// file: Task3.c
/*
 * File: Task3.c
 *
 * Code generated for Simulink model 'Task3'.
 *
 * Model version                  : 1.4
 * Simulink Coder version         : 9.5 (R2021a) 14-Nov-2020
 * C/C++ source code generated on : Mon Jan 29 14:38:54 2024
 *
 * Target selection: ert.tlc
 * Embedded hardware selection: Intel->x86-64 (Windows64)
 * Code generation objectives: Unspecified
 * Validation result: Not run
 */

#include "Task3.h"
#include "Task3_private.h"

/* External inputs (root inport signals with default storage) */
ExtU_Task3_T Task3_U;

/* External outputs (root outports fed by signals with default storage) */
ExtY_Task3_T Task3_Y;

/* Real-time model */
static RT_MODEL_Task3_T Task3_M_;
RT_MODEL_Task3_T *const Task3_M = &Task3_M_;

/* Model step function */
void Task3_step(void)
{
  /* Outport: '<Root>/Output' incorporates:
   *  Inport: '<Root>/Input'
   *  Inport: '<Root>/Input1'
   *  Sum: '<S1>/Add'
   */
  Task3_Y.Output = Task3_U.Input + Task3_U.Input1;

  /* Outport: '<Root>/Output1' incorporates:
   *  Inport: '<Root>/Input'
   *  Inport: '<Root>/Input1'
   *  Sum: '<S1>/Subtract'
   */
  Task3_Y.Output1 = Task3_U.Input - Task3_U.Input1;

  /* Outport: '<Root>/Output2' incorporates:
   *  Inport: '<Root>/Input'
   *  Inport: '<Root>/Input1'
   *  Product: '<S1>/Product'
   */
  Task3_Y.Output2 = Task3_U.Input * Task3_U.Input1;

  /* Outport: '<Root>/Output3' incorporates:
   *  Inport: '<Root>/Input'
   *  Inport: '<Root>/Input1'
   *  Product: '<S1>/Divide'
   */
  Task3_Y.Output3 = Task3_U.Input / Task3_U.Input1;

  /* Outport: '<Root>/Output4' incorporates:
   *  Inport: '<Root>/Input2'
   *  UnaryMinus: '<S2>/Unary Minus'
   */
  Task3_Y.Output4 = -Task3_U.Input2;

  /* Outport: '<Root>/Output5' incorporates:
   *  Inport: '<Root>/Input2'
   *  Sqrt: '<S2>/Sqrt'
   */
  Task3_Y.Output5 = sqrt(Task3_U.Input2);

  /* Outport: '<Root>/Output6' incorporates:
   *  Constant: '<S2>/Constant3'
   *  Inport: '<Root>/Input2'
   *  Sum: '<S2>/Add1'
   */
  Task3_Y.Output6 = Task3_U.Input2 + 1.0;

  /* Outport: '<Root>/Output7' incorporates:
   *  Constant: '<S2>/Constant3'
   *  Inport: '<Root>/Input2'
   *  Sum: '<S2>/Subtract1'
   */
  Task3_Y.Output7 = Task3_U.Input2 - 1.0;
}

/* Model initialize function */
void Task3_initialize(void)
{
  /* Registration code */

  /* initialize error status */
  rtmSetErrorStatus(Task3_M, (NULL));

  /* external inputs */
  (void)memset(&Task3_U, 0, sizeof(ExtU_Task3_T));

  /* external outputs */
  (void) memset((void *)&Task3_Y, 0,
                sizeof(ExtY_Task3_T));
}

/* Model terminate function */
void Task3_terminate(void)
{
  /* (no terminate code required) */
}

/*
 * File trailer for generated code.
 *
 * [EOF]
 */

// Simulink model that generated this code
simulink model "Task3"  (R2021a)
settings: Solver=FixedStepDiscrete  StartTime=0.0  StopTime=10.0  RelTol=1e-3  EnableMultiTasking=on

== system Task3 ==
  Input : Inport
  Input1 : Inport  Port=2
  Input2 : Inport  Port=3
  Subsystem : Subsystem
  Subsystem1 : Subsystem
  Output : Outport
  Output1 : Outport  Port=2
  Output2 : Outport  Port=3
  Output3 : Outport  Port=4
  Output4 : Outport  Port=5
  Output5 : Outport  Port=6
  Output6 : Outport  Port=7
  Output7 : Outport  Port=8
  wires:
  Input/1 -> Subsystem/1(In1)
  Input1/1 -> Subsystem/2(In2)
  Subsystem/1(Out1) -> Output/1
  Subsystem/2(Out2) -> Output1/1
  Subsystem/3(Out3) -> Output2/1
  Subsystem/4(Out4) -> Output3/1
  Input2/1 -> Subsystem1/1(In1)
  Subsystem1/1(Out1) -> Output4/1
  Subsystem1/2(Out2) -> Output5/1
  Subsystem1/3(Out3) -> Output6/1
  Subsystem1/4(Out4) -> Output7/1

== system Task3/Subsystem ==
  In1 : Inport
  In2 : Inport  Port=2
  Add : Sum
  Divide : Product  Inputs=*/
  Product : Product
  Subtract : Sum  Inputs=+-
  Out1 : Outport
  Out2 : Outport  Port=2
  Out3 : Outport  Port=3
  Out4 : Outport  Port=4
  wires:
  In1/1 -> Add/1, Divide/1, Product/1, Subtract/1
  In2/1 -> Add/2, Subtract/2, Divide/2, Product/2
  Divide/1 -> Out4/1
  Product/1 -> Out3/1
  Subtract/1 -> Out2/1
  Add/1 -> Out1/1

== system Task3/Subsystem1 ==
  In1 : Inport
  Add1 : Sum
  Constant3 : Constant
  Sqrt : Sqrt  SaturateOnIntegerOverflow=on
  Subtract1 : Sum  Inputs=+-
  Unary Minus : UnaryMinus  SaturateOnIntegerOverflow=on
  Out1 : Outport
  Out2 : Outport  Port=2
  Out3 : Outport  Port=3
  Out4 : Outport  Port=4
  wires:
  In1/1 -> Subtract1/1, Add1/1, Unary Minus/1, Sqrt/1
  Add1/1 -> Out3/1
  Constant3/1 -> Add1/2, Subtract1/2
  Subtract1/1 -> Out4/1
  Unary Minus/1 -> Out1/1
  Sqrt/1 -> Out2/1
